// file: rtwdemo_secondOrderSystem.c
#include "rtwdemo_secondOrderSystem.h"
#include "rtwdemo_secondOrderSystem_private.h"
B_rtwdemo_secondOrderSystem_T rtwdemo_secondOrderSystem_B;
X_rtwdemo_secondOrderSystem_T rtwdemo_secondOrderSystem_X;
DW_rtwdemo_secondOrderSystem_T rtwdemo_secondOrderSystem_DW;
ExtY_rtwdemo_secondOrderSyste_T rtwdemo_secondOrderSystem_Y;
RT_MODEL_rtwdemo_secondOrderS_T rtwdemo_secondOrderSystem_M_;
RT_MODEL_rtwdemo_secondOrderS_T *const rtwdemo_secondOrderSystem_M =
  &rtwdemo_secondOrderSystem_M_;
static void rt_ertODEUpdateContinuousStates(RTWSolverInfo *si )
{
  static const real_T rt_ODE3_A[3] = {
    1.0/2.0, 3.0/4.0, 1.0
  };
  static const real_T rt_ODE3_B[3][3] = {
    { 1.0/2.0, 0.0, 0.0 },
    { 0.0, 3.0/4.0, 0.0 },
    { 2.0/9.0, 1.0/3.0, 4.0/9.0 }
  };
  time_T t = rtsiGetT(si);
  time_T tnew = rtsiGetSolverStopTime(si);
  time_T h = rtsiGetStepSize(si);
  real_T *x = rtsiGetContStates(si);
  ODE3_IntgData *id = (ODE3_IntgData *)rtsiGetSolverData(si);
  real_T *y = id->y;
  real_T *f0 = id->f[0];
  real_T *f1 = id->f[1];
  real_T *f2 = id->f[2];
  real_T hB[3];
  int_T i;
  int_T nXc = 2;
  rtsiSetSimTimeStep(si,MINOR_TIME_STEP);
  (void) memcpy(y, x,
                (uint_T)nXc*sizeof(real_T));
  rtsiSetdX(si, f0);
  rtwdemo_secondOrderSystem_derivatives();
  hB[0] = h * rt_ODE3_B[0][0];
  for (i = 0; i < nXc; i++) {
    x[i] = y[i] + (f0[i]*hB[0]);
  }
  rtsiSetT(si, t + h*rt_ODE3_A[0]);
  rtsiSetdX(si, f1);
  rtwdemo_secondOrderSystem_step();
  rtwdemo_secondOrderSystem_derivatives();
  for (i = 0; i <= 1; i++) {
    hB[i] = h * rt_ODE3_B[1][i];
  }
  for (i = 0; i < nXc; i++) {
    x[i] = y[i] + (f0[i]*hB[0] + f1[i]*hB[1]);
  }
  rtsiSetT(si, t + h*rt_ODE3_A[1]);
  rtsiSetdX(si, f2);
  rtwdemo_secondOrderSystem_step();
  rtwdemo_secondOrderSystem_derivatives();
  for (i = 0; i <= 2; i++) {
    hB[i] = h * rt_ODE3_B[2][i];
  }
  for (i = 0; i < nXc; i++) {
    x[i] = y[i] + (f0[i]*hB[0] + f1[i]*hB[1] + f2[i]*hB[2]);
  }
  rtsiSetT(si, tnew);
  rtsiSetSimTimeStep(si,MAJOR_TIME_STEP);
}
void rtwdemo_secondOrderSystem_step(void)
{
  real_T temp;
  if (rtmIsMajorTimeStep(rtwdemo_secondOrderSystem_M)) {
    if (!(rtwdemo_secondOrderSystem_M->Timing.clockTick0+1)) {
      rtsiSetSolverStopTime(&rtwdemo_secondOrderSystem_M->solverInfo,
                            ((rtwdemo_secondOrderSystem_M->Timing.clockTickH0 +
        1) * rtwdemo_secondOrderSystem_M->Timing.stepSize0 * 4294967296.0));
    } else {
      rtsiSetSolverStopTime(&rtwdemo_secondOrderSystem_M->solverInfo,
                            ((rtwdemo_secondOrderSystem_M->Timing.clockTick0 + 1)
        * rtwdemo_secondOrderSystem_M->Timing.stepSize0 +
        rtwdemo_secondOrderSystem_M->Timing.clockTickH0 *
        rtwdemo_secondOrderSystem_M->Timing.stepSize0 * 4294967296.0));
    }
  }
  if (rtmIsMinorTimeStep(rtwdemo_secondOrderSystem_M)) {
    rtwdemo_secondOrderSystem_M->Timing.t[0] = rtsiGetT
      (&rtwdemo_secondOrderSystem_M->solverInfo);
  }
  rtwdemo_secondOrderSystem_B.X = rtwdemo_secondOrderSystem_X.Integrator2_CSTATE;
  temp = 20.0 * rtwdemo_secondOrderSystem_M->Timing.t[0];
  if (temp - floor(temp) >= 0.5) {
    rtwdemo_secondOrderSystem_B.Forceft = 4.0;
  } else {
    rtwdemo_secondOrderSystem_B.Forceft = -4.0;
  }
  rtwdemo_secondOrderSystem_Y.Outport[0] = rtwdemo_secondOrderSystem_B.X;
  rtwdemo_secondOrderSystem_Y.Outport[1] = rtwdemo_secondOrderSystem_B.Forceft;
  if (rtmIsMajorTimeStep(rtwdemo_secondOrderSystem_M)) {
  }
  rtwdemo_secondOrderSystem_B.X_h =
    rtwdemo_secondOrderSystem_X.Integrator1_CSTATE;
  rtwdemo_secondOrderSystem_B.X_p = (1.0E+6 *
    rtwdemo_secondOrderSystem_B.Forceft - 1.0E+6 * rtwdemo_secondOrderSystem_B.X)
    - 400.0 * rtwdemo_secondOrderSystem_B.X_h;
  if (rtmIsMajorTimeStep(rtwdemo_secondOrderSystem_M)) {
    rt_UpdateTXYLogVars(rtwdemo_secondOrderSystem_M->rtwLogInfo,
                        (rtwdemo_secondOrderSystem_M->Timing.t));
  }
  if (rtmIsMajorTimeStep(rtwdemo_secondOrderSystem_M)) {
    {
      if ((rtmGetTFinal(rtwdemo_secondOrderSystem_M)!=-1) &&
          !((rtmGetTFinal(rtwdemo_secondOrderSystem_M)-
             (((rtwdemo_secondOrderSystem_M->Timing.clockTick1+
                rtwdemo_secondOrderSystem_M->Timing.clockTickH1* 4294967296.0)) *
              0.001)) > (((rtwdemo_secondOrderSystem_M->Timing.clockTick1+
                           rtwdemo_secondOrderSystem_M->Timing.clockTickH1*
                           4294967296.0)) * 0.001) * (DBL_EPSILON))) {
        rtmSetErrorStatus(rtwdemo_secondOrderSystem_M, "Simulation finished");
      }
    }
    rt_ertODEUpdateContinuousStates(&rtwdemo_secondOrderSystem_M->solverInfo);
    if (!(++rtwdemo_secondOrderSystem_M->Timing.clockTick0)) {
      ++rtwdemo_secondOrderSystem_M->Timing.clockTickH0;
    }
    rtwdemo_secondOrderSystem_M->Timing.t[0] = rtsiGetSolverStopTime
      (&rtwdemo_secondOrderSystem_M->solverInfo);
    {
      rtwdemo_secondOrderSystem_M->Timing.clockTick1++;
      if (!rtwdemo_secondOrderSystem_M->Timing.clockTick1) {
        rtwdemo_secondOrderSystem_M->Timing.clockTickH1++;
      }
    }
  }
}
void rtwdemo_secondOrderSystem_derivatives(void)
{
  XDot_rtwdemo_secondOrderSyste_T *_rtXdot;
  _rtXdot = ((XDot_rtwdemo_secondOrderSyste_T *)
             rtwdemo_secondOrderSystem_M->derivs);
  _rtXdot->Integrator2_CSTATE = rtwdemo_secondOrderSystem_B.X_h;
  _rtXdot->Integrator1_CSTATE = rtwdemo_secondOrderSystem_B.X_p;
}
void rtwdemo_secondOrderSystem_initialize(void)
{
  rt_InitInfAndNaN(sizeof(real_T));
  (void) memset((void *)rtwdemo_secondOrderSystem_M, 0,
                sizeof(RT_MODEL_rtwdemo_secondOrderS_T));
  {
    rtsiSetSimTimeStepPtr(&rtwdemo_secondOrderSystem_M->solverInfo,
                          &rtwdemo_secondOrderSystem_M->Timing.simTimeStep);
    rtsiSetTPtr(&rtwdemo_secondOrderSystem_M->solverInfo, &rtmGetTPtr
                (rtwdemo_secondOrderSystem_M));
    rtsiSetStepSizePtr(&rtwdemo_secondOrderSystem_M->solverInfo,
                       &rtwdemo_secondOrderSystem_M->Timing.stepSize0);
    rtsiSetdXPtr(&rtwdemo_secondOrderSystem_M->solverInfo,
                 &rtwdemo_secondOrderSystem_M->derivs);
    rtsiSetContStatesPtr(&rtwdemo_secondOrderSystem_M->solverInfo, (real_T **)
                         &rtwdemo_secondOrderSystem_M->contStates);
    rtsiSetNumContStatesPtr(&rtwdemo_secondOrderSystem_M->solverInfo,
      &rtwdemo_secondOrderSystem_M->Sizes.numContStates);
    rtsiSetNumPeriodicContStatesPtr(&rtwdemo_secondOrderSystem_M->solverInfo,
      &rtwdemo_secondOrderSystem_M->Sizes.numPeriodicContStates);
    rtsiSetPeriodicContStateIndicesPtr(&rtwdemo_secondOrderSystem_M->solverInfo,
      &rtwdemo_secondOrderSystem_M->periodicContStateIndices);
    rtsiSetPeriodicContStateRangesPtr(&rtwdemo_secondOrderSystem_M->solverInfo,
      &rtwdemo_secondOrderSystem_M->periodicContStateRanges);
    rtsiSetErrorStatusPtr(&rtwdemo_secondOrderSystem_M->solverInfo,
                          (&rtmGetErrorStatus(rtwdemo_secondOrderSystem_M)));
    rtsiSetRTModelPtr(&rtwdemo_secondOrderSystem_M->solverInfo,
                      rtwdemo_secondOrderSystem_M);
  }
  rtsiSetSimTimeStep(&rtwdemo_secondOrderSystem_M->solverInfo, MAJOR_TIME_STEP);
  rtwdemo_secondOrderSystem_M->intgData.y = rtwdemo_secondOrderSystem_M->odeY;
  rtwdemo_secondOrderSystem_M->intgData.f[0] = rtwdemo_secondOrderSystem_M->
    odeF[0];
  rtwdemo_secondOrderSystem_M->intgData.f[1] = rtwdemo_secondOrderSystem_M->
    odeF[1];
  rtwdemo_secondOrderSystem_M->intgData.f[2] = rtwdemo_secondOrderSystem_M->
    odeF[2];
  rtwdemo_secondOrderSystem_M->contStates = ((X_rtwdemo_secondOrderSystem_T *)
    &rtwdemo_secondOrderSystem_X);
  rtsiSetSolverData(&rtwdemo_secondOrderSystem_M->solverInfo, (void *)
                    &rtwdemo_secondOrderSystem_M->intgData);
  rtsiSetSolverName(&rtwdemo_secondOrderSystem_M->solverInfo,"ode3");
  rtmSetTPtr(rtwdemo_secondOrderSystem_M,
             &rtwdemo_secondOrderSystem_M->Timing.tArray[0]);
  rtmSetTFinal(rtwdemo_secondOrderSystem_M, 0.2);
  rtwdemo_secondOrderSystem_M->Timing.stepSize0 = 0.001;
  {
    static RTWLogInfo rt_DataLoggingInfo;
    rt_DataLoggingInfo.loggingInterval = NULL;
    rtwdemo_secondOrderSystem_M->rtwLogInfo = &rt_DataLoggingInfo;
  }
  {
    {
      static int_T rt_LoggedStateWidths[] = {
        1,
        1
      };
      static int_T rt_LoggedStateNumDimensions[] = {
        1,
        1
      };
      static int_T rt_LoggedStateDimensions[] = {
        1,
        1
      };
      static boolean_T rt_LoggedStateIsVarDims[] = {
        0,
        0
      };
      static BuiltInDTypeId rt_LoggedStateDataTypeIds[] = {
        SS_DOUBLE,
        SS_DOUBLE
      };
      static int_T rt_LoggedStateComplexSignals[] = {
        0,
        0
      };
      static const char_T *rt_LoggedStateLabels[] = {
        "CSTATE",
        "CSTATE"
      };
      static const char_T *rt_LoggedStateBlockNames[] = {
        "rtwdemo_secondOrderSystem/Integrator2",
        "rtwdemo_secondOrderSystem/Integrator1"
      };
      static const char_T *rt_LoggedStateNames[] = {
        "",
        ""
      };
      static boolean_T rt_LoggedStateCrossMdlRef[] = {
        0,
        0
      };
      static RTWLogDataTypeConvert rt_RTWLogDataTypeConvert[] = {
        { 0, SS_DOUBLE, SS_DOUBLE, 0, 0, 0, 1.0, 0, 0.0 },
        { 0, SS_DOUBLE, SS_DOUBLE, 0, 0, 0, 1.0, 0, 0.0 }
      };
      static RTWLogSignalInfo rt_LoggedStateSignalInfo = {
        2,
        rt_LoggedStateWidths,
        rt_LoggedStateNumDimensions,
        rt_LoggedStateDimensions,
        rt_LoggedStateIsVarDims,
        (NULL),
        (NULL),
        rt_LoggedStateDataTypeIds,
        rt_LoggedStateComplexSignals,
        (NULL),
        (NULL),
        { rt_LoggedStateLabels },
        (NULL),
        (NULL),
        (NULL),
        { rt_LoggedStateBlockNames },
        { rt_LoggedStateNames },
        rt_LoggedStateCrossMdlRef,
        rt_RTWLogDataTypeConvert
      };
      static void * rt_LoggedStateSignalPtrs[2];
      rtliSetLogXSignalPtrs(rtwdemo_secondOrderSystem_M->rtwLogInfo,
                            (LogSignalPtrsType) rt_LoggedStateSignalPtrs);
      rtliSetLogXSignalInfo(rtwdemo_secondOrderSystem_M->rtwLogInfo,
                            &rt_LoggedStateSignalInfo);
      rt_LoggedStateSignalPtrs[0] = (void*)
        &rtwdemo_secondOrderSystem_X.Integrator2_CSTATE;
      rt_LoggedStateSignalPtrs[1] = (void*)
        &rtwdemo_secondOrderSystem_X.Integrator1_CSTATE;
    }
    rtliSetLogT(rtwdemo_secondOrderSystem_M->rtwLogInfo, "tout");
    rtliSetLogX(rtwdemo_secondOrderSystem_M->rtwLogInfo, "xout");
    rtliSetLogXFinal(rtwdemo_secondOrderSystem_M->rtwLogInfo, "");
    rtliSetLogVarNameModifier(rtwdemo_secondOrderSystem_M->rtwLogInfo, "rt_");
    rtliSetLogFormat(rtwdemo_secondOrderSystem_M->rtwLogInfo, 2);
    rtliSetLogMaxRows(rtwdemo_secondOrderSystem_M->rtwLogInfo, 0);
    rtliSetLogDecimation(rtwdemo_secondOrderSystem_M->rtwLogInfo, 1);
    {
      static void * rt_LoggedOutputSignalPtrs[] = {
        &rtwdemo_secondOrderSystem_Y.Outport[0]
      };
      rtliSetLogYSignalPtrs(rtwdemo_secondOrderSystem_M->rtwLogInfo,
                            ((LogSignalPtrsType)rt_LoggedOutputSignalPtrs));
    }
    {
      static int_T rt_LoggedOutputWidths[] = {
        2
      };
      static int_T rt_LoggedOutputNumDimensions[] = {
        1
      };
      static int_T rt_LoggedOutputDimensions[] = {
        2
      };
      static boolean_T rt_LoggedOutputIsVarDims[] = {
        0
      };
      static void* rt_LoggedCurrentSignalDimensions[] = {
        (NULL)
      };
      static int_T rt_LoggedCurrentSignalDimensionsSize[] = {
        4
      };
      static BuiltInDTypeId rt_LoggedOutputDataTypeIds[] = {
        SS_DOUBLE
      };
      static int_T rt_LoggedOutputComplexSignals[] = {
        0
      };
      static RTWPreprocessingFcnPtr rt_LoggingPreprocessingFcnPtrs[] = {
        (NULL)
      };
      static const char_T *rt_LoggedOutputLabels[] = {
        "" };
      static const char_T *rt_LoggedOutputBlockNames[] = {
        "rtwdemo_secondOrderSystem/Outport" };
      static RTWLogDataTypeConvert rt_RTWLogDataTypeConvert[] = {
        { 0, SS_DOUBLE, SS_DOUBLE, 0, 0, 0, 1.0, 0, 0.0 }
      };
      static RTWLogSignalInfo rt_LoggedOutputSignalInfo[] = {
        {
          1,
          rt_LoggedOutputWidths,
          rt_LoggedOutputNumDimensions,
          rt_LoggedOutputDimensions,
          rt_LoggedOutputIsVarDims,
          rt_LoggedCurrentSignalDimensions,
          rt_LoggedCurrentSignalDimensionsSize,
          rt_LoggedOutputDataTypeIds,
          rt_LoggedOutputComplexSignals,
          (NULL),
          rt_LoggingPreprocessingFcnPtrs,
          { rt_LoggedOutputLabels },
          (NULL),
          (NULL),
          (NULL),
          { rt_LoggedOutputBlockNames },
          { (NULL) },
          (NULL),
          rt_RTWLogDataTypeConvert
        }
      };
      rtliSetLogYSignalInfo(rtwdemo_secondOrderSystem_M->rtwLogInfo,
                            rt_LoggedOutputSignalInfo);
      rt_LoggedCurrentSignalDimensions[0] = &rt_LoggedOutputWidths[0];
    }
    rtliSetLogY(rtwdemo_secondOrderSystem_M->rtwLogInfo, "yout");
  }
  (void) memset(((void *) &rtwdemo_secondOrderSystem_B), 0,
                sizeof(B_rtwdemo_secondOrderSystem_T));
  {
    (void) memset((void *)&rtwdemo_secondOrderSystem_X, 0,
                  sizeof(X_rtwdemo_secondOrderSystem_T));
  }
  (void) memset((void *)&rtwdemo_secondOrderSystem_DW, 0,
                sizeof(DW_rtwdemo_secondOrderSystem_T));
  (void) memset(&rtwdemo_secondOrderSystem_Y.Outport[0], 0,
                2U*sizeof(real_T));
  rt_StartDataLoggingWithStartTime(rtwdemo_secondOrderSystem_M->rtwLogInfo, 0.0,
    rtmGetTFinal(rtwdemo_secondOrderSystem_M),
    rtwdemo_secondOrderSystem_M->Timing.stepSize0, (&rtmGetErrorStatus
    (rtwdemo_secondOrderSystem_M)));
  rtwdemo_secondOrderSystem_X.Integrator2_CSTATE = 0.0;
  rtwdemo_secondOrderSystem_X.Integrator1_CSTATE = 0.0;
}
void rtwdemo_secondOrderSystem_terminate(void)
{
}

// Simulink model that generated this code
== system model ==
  Outport : Outport  InitialOutput=0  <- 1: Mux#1
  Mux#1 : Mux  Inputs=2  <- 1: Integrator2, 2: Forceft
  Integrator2 : Integrator  <- 1: Integrator1
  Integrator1 : Integrator  <- 1: Sum#1
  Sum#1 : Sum  Inputs=-+-  <- 1: Gain#1, 2: Gain#2, 3: Gain#3
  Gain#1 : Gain  Gain=1000000  <- 1: Integrator2
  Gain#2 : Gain  Gain=1000000  <- 1: Forceft
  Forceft : SignalGenerator  Amplitude=4  Frequency=20
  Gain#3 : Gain  Gain=400  <- 1: Integrator1
